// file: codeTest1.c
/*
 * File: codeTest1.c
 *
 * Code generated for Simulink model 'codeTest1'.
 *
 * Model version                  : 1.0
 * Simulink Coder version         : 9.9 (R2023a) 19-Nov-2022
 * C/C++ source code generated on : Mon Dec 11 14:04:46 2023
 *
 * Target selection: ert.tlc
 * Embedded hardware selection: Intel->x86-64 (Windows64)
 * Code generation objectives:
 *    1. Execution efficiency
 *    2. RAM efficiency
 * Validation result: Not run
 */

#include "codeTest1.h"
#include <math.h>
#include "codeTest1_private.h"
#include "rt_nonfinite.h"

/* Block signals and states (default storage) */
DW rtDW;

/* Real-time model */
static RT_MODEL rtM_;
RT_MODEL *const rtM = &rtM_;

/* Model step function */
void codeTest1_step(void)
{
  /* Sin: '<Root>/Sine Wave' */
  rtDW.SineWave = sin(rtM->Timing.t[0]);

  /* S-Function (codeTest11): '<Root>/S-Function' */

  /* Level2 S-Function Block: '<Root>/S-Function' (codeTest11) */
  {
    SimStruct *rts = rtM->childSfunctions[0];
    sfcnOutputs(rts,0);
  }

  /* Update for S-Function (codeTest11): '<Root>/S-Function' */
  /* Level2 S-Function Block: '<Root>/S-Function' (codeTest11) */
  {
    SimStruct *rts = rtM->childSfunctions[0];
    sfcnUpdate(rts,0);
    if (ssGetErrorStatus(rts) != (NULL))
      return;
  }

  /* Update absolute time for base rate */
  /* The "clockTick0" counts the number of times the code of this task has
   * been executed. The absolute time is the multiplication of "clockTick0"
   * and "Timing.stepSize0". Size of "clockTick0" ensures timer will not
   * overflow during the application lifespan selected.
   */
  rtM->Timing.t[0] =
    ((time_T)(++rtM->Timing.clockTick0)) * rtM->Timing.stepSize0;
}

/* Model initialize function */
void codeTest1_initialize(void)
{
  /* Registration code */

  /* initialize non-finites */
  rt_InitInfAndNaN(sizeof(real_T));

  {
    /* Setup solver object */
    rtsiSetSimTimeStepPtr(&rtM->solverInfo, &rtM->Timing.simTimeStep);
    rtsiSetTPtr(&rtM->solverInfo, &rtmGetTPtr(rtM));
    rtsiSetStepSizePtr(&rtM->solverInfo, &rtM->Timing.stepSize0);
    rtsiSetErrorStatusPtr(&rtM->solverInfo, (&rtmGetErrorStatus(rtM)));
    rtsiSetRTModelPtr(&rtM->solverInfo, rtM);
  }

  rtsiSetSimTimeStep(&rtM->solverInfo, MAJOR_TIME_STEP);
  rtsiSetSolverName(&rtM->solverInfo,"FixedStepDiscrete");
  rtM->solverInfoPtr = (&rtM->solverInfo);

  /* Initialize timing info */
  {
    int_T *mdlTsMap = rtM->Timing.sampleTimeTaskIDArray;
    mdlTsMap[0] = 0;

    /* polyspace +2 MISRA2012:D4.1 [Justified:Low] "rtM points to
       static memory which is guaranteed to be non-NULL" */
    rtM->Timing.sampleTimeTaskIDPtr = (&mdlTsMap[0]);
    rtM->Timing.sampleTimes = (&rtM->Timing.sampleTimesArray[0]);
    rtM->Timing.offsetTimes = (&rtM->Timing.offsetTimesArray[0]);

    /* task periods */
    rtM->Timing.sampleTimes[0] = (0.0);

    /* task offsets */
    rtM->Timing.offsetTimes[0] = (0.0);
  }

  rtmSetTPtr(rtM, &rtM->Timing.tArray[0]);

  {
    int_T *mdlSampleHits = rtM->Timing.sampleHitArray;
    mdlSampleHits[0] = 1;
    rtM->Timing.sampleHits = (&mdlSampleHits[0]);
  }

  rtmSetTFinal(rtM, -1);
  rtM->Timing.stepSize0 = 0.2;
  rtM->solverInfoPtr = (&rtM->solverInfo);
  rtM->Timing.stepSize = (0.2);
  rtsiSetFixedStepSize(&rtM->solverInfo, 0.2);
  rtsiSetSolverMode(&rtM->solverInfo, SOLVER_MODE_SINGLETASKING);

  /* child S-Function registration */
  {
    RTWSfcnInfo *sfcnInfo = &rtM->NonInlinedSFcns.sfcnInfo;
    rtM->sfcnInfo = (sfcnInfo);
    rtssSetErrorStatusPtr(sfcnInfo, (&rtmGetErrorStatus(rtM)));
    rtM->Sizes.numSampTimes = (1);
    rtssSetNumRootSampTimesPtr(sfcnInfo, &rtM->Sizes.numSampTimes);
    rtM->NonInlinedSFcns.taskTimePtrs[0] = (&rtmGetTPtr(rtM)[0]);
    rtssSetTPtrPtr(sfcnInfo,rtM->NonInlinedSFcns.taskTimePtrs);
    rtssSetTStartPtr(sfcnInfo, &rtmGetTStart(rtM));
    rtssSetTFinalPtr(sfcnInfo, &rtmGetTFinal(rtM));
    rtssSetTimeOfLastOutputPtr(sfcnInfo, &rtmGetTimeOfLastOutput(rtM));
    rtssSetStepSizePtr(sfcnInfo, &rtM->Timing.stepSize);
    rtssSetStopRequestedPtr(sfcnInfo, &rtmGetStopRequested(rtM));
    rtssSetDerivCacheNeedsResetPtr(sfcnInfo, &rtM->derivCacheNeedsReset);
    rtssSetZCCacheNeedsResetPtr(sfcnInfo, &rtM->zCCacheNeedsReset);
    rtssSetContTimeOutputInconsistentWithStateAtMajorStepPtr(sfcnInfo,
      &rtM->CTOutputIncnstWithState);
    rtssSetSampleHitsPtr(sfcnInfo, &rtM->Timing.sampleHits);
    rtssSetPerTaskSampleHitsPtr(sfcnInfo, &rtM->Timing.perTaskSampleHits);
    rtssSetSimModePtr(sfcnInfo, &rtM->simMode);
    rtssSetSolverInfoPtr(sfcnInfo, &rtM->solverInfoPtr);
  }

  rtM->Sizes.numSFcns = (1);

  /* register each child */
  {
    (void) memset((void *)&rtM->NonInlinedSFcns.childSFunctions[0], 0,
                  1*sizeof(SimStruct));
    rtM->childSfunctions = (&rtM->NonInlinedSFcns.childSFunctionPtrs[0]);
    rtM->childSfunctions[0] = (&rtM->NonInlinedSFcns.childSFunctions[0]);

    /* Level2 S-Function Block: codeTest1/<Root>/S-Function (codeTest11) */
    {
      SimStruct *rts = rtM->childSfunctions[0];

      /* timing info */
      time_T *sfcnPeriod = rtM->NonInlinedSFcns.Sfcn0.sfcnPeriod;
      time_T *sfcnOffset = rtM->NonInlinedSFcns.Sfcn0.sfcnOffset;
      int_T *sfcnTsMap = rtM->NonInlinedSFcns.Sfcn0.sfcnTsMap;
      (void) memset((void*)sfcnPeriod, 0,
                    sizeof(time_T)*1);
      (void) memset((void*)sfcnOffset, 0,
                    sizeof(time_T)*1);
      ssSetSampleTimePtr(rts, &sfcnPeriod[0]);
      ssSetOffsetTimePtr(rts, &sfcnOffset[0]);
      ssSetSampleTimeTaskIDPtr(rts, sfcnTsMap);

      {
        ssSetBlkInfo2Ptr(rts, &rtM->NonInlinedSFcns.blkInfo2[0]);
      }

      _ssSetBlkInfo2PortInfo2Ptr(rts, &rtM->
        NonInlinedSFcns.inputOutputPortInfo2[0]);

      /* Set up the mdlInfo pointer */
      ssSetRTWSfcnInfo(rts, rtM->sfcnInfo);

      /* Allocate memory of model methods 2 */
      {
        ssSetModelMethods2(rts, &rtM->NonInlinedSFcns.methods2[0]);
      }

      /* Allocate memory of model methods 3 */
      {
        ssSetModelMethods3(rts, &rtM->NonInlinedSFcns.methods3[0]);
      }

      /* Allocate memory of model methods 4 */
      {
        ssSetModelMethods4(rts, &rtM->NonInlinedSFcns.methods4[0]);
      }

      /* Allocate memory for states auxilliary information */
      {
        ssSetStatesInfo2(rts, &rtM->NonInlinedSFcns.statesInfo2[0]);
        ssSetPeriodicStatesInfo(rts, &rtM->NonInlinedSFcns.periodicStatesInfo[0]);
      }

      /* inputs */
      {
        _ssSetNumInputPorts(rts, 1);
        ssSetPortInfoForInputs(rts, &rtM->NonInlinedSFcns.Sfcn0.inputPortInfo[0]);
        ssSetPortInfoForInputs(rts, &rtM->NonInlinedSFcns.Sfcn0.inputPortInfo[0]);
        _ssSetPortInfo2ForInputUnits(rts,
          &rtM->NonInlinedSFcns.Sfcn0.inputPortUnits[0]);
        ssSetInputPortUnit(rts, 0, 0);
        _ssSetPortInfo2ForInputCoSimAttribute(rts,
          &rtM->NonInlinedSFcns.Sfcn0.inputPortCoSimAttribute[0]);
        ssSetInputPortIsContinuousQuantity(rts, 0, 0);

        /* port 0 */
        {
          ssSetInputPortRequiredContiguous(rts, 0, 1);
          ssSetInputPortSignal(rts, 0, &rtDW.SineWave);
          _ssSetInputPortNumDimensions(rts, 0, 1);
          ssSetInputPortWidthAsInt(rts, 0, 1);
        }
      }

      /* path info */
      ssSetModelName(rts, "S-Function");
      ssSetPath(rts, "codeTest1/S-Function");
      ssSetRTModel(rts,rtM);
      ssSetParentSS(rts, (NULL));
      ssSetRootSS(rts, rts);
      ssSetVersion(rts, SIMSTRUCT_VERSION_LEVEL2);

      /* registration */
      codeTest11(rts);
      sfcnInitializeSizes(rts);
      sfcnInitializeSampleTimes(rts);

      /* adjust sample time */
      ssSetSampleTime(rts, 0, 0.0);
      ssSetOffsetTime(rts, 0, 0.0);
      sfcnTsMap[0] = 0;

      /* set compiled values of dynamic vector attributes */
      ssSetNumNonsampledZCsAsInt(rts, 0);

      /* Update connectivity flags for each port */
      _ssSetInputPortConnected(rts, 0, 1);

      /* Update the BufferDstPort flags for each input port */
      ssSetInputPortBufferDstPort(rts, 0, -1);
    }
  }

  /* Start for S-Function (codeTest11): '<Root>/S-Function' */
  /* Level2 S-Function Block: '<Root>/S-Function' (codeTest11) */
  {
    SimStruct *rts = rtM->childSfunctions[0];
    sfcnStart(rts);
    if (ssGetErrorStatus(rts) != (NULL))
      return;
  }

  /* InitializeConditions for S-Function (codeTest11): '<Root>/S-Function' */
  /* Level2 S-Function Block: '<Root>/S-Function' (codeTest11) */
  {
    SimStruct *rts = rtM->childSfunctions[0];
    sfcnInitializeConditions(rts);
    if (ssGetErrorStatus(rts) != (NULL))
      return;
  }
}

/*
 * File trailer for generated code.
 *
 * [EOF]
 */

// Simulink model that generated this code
simulink model "codeTest1"  (R2023a)
settings: Solver=FixedStepDiscrete  StartTime=0.0  StopTime=10.0  RelTol=1e-3

== system codeTest1 ==
  S-Function : S-Function  FunctionName=codeTest11  SFunctionDeploymentMode=off  EnableBusSupport=off
  Sine Wave : Sin  SampleTime=0
  wires:
  Sine Wave/1 -> S-Function/1
